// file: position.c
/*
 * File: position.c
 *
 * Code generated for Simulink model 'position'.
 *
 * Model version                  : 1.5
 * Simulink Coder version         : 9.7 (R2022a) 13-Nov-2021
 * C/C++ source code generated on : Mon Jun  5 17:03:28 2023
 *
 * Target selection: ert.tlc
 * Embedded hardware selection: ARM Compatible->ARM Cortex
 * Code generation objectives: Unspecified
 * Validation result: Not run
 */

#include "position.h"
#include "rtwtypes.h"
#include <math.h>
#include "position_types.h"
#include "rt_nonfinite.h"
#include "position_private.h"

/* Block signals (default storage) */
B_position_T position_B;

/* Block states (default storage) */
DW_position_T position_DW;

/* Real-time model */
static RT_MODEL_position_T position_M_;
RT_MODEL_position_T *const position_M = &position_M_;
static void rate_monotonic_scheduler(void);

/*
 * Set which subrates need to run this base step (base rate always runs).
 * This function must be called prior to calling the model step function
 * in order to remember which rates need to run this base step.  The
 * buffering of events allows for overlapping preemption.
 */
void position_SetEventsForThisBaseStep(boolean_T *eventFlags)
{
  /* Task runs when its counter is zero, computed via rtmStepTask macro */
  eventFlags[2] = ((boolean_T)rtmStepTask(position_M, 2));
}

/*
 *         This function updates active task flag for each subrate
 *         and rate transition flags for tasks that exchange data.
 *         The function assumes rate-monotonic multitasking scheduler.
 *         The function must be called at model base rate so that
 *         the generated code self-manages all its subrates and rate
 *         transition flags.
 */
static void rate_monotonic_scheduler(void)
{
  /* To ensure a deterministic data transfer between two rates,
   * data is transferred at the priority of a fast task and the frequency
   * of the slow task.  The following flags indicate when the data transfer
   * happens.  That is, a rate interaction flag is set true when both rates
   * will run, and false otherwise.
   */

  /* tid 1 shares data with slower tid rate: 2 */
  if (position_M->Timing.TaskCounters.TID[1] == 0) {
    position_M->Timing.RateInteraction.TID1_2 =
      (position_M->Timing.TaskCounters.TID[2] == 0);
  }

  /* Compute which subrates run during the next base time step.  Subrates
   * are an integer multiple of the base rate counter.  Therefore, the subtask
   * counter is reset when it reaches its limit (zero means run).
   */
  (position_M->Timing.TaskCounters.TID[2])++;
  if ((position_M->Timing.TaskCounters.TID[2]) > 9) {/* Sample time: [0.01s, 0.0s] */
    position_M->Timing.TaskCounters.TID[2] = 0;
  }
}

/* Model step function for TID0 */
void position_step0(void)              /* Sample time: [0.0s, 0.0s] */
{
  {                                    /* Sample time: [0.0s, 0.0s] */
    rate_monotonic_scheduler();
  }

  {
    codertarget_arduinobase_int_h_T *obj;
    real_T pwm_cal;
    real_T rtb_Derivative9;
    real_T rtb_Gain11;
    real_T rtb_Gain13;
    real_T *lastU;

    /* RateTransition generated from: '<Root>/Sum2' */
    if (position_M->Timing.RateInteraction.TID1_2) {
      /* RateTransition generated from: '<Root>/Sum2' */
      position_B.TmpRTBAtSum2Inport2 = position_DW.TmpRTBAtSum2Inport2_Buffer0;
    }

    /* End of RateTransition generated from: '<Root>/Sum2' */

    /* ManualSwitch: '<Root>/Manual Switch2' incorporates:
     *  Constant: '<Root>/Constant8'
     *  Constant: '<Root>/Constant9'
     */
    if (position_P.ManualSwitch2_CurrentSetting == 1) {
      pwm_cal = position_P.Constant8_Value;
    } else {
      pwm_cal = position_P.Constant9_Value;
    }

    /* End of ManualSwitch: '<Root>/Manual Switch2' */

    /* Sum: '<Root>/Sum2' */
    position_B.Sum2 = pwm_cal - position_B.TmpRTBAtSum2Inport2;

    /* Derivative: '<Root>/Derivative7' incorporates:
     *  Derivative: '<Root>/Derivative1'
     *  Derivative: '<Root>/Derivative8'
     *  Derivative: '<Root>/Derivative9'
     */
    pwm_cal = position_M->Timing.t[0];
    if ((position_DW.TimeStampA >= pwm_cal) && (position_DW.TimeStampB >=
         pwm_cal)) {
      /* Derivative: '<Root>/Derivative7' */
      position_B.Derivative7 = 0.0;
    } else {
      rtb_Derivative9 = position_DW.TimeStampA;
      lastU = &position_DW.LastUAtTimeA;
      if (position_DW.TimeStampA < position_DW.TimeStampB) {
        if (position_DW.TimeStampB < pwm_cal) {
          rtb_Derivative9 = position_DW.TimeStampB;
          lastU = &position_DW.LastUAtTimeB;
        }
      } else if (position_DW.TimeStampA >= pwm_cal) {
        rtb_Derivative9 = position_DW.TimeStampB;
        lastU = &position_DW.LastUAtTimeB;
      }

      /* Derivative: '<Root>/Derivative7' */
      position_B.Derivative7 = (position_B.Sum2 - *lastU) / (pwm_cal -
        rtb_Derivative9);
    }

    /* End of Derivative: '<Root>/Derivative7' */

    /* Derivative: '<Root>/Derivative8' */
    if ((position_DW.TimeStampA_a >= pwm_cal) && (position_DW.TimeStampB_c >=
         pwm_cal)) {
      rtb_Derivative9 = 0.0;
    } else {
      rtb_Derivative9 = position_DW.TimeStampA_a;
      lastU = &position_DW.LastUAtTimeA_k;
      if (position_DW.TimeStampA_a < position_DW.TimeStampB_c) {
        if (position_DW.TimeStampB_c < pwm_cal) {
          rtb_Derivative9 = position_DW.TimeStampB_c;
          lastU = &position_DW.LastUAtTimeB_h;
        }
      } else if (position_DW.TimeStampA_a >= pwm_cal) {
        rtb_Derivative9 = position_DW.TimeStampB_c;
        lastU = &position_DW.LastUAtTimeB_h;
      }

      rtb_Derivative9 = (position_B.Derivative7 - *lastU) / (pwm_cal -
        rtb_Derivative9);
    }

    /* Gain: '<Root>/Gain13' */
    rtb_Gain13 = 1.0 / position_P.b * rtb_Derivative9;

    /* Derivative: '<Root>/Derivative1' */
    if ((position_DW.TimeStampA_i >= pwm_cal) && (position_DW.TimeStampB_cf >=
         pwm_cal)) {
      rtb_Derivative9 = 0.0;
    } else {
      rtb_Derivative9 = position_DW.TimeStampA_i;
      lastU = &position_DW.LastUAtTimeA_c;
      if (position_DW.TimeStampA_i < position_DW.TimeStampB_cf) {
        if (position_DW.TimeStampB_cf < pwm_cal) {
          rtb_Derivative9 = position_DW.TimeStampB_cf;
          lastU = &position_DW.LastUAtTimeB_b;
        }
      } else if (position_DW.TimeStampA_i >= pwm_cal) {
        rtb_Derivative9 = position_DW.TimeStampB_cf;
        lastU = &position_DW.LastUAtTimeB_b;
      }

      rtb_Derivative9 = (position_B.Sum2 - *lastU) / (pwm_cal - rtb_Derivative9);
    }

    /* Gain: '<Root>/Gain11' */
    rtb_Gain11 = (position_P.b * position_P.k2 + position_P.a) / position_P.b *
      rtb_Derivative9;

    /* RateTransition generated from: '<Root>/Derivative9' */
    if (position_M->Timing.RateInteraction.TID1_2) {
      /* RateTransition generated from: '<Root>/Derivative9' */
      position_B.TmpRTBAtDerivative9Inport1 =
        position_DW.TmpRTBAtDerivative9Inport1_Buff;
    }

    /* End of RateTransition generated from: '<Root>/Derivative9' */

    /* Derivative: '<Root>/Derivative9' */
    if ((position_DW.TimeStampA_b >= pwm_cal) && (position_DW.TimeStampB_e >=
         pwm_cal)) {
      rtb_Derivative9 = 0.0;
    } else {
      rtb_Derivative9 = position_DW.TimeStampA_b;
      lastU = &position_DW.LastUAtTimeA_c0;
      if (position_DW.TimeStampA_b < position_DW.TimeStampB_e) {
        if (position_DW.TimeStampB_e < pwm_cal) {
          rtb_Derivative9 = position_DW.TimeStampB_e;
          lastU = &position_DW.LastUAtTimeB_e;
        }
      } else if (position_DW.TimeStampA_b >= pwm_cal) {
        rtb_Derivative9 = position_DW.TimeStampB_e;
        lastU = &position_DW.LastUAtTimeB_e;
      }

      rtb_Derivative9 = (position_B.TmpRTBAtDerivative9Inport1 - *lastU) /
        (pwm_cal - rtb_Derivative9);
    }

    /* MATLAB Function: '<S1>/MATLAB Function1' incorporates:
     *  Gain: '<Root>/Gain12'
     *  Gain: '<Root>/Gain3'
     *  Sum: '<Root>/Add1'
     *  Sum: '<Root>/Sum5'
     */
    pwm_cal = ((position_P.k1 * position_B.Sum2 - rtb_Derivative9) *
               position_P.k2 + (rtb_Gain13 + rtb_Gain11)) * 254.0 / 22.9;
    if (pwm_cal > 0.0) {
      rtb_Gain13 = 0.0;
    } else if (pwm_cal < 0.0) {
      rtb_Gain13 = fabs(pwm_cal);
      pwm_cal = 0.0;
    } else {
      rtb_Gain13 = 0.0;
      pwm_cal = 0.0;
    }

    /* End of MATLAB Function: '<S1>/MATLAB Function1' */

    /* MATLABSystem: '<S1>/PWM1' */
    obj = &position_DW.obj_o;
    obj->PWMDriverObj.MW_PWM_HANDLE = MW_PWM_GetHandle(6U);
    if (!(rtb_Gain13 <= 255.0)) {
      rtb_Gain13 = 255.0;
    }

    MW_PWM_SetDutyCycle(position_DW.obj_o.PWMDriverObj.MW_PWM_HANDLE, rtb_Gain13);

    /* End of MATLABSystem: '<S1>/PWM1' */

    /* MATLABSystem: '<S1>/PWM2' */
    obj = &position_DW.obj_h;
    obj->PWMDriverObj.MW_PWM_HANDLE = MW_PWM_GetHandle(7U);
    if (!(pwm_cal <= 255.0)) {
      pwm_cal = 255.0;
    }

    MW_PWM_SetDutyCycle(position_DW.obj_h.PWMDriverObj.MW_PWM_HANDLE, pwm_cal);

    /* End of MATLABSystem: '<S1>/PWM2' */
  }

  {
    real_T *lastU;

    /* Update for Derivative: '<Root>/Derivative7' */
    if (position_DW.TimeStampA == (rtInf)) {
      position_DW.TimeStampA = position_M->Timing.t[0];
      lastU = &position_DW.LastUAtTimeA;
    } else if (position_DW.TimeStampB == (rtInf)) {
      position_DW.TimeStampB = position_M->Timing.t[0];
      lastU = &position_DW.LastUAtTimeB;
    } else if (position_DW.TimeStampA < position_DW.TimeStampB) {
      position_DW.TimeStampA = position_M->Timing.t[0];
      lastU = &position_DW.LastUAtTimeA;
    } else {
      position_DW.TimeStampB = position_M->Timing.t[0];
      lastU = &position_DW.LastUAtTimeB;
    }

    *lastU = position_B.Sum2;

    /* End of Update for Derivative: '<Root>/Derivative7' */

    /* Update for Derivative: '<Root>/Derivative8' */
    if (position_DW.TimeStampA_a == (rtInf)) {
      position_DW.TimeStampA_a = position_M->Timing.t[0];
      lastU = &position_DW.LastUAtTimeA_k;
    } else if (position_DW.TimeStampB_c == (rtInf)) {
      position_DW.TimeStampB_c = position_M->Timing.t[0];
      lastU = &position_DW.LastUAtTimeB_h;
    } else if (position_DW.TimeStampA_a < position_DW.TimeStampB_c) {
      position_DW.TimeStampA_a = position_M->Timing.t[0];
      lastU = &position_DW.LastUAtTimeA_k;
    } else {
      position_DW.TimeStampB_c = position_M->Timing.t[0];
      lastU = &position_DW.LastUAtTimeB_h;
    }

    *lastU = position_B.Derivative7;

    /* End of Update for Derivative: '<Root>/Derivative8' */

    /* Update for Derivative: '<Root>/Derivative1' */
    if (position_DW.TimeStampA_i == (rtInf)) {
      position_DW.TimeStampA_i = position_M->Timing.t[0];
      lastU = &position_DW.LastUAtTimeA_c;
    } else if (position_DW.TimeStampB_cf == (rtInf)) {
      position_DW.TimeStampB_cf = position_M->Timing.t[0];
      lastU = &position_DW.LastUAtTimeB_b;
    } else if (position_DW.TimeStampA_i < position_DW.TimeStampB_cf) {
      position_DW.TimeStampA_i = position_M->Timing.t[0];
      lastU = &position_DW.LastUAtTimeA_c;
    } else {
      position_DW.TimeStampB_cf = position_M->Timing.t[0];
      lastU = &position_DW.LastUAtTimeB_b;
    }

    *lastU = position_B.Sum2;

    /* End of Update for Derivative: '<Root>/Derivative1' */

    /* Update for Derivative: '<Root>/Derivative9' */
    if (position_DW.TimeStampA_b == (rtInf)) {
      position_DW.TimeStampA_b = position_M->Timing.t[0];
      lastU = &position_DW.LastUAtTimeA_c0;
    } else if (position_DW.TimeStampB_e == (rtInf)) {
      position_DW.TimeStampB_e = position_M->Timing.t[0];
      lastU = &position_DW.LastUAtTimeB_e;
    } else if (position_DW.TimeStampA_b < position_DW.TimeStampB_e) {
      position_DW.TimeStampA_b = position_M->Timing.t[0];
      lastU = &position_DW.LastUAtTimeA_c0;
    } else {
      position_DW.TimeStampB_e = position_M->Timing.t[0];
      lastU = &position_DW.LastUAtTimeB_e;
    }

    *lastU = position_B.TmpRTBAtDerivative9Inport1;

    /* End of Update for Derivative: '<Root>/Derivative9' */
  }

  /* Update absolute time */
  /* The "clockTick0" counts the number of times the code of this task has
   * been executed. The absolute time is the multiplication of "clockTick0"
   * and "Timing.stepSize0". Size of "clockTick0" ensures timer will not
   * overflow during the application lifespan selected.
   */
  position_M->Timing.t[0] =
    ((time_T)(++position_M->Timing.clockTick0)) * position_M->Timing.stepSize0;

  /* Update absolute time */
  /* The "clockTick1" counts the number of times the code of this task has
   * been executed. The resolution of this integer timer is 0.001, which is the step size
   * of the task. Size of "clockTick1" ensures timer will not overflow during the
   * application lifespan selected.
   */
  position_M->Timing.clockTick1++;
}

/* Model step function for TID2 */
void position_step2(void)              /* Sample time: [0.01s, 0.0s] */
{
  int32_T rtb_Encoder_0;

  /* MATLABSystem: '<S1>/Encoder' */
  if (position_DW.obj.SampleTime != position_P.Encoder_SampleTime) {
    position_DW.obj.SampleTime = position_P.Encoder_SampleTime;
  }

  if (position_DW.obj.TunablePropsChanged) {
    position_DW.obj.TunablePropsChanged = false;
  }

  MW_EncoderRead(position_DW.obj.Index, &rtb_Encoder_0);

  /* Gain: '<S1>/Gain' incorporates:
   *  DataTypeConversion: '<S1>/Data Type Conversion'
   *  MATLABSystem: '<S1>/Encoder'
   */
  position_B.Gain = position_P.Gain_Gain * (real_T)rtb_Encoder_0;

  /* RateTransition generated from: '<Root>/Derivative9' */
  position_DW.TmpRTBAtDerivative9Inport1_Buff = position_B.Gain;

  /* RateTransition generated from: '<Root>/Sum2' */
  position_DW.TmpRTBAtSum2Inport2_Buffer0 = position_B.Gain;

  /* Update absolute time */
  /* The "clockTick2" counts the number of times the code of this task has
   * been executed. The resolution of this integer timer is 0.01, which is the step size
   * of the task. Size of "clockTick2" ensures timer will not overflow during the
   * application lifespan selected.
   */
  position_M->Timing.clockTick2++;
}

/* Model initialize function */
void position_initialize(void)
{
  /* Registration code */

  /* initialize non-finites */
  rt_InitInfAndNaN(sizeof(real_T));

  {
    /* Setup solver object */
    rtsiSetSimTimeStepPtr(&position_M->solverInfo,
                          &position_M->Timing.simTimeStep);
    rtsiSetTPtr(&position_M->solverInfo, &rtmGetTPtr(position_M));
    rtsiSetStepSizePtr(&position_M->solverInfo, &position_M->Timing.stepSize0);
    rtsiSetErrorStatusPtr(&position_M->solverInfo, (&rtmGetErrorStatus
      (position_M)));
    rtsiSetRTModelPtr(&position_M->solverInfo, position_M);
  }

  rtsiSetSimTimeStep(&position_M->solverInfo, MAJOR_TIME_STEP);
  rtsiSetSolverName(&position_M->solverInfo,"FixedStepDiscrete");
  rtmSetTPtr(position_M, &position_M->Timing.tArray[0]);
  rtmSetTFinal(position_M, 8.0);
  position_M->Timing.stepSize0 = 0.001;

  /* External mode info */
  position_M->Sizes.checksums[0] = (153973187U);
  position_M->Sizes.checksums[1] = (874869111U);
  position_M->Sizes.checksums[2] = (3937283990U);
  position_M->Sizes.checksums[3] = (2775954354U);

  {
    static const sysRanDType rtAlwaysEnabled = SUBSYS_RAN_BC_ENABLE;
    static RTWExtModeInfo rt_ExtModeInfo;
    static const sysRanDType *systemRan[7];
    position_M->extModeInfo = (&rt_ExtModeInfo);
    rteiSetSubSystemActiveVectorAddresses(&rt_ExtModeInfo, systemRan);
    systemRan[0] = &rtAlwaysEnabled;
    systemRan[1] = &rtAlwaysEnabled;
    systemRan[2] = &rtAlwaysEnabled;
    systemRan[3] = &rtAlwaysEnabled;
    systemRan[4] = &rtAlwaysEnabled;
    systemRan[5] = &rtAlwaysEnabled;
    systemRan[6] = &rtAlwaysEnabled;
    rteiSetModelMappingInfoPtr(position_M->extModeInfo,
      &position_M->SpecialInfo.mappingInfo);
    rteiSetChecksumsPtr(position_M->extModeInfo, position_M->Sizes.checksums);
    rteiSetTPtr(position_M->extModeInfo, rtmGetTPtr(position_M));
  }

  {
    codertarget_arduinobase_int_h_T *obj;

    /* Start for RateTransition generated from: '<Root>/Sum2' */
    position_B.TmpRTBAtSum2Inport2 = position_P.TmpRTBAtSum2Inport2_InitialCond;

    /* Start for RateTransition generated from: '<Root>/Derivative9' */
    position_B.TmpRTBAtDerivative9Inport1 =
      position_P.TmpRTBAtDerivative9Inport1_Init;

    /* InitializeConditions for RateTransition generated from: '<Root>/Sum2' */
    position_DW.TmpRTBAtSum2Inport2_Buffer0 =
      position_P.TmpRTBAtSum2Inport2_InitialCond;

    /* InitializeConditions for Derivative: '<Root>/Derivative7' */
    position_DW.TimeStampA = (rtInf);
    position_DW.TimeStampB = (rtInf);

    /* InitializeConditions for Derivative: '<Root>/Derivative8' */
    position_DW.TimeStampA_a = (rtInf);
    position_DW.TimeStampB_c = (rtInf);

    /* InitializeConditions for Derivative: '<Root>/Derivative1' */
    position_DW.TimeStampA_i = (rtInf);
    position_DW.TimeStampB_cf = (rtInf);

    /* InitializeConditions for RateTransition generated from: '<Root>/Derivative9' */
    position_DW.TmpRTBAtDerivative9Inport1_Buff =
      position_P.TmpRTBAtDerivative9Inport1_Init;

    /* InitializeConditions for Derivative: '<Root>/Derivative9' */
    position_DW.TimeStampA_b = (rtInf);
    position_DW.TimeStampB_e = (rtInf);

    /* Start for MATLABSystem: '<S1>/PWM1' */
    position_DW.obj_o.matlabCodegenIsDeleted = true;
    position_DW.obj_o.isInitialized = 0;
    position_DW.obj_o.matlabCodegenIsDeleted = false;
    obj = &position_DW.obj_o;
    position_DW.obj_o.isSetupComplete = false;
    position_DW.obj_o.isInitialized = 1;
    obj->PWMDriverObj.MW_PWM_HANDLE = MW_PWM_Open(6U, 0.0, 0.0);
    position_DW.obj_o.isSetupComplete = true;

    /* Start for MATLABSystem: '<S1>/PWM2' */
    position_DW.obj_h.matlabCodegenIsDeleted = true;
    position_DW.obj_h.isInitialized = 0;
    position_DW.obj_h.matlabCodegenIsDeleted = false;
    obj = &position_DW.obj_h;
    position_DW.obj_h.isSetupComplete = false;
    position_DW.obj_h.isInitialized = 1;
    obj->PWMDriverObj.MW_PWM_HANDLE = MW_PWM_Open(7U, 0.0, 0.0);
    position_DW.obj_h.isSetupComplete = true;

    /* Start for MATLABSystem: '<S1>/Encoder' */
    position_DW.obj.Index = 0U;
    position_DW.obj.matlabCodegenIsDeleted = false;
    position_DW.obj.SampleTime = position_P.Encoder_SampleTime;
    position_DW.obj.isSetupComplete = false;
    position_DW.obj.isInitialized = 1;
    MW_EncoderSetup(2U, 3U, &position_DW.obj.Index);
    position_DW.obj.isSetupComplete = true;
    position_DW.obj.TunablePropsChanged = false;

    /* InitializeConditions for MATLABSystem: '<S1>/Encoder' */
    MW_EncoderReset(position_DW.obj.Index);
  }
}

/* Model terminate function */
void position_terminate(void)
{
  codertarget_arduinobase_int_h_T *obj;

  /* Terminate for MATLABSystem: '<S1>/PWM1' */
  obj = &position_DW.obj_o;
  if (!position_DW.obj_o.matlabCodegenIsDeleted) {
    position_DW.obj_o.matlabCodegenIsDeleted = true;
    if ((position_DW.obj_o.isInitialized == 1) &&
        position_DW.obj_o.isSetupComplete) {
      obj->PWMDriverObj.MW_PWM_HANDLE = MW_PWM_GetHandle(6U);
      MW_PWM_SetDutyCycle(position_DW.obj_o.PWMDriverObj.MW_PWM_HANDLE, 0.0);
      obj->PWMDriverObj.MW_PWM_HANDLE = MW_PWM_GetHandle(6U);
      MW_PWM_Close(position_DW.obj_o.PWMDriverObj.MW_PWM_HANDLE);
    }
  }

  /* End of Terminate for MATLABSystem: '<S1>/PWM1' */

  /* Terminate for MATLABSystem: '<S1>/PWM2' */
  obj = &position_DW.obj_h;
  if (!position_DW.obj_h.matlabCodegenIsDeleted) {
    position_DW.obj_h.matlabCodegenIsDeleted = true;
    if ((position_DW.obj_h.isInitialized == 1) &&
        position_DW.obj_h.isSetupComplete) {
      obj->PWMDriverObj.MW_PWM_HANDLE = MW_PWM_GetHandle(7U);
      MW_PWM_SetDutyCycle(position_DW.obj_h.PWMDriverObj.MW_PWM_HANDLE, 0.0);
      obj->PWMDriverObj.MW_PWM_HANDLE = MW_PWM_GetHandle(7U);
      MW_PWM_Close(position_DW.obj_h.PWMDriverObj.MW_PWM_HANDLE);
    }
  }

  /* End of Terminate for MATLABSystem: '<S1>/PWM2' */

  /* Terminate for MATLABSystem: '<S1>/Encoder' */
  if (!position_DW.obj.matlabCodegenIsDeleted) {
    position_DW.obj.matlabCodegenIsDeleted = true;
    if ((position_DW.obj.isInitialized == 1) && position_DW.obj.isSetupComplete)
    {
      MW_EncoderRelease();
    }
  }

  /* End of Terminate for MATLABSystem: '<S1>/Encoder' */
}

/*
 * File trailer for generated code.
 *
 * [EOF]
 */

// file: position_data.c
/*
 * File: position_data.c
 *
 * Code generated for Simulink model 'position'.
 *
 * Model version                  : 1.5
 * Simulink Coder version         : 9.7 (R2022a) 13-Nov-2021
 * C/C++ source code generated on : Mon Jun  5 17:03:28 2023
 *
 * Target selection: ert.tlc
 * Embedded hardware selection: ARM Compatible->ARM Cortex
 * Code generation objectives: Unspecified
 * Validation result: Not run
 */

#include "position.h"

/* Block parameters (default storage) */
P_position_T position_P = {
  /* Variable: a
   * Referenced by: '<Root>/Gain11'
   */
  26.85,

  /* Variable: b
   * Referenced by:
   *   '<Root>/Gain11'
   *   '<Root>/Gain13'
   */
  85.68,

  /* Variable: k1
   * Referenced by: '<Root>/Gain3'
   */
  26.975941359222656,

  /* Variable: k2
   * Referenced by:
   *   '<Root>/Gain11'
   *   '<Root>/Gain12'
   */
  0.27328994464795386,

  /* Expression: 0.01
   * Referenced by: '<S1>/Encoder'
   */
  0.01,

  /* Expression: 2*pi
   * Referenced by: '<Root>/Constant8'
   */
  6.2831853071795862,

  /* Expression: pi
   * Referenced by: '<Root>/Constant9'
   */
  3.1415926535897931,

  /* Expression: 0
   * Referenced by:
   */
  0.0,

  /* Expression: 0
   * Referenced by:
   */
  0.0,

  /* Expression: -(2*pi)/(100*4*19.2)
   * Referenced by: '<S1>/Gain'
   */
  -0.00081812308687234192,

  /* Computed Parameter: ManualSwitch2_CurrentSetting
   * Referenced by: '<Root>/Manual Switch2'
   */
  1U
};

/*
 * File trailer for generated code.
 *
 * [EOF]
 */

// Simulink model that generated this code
simulink model "position"  (R2022a)
settings: Solver=ode1  StartTime=0.0  StopTime=8  FixedStep=0.001  RelTol=1e-3  EnableMultiTasking=on
undefined symbols (not defined in the file): a, b, k1, k2
libraries: arduinolib x4, arduinosensorlib x1

== system position ==
  note: $\theta$
  Add1 : Sum  Inputs=+++
  Constant8 : Constant  Value=2*pi
  Constant9 : Constant  Value=pi
  Derivative{1,7..9} (4 alike) : Derivative
  Gain11 : Gain  Gain=(a+b*k2)/b
  Gain12 : Gain  Gain=k2
  Gain13 : Gain  Gain=1/b
  Gain3 : Gain  Gain=k1
  Manual Switch2 : ManualSwitch
  Right motor1 : Subsystem
  Scope1 : Scope
  Scope7 : Scope
  Sum2 : Sum  Inputs=|+-
  Sum5 : Sum  Inputs=|+-
  wires:
  Right motor1/1(outGearBox) -> Sum2/2, Derivative9/1, Scope7/1
  Derivative8/1 -> Gain13/1
  Add1/1 -> Right motor1/1(v_a)
  Constant9/1 -> Manual Switch2/2
  Sum2/1 -> Scope1/1, Derivative7/1, Derivative1/1, Gain3/1
  Gain11/1 -> Add1/2
  Derivative9/1 -> Sum5/2
  Manual Switch2/1 -> Sum2/1
  Derivative1/1 -> Gain11/1
  Gain3/1 -> Sum5/1
  Constant8/1 -> Manual Switch2/1
  Gain13/1 -> Add1/1
  Derivative7/1 -> Derivative8/1
  Gain12/1 -> Add1/3
  Sum5/1 -> Gain12/1

== system position/Right motor1 ==
  v_a : Inport
  Convert pulse to rad1 : MATLAB Function  Commented=on  TreatAsAtomicUnit=on
  Data Type Conversion : DataTypeConversion  OutDataTypeStr=double  SaturateOnIntegerOverflow=off  RndMeth=Floor
  Digital Output : arduinolib/Digital Output  Commented=on  pinNumber=7  Direction=output  blockPlatform=arduino
  Encoder : arduinosensorlib/Encoder  InputA=2  InputB=3  Mode=No reset  SampleTime=0.01
  Encoder1 : S-Function  Commented=on  InitFcn=try, set_param(gcb,'FunctionName','readEncDUEpin8_9'), end  FunctionName=readEncDUEpin8_9  SFunctionModules=readEncDUEpin8_9_wrapper  SFunctionDeploymentMode=off  EnableBusSupport=off  mask(S-Function Builder){}
      mask help: Simulink:masks:SFunctionBuilder_MD
      mask init:
      | val = [[.9  0.75 0.75 1 1 .9 .9 1]',[1 1 0.75 0.75 .9 .9 1 .9]'];try , sys = get_param(gcb,'SfunBuilderFcnName');if isempty(sys), sys = get_param(gcb,'FunctionName'); end,catch, sys = get_param(gcb,'FunctionName'); end
  Gain : Gain  Gain=-(2*pi)/(100*4*19.2)
  MATLAB Function1 : MATLAB Function  TreatAsAtomicUnit=on
  MATLAB Function2 : MATLAB Function  Commented=on  TreatAsAtomicUnit=on
  PWM : arduinolib/PWM  Commented=on  pinNumber=5  frequencyType=Default  desiredFrequency=490.2  achievableFrequency=490.2
  PWM1 : arduinolib/PWM  pinNumber=6  frequencyType=Default  desiredFrequency=490.2  achievableFrequency=490.2
  PWM2 : arduinolib/PWM  pinNumber=7  frequencyType=Default  desiredFrequency=490.2  achievableFrequency=490.2
  Scope : Scope  Commented=on
  Scope1 : Scope
  gearRatio : Constant  Commented=on  Value=336
  totalPPR : Constant  Commented=on  Value=16*2
  outGearBox : Outport
  wires:
  Gain/1 -> Scope1/1, outGearBox/1
  Encoder/1 -> Data Type Conversion/1
  v_a/1 -> MATLAB Function1/1(v_a)
  MATLAB Function1/2(Rpwm) -> PWM2/1
  MATLAB Function1/1(Lpwm) -> PWM1/1
  Encoder1/1 -> Convert pulse to rad1/1(u)
  Convert pulse to rad1/1(outGearBox) -> Scope/1
  gearRatio/1 -> Convert pulse to rad1/3(gearRatio)
  MATLAB Function2/1(pwm) -> PWM/1
  MATLAB Function2/2(dir) -> Digital Output/1
  totalPPR/1 -> Convert pulse to rad1/2(ppr)
  Data Type Conversion/1 -> Gain/1

== matlab function position/Right motor1/Convert pulse to rad1 ==
  settings: updateMethod=DISCRETE
function outGearBox = fcn(u,ppr,gearRatio)

persistent counter_num over_flag
if(isempty(counter_num)), counter_num = 0;end
if(isempty(over_flag)), over_flag = 0;end
pulse2radian = 2*pi/ppr; % 1 pulse = ?? radian

if(double(u) - counter_num > 40000), over_flag = over_flag-1;
elseif(double(u) - counter_num < -40000), over_flag = over_flag+1;
end

inGearBox = (double(u)+over_flag*(2^32 -1))*pulse2radian; 
outGearBox = inGearBox/gearRatio;
counter_num = double(u) ;

== matlab function position/Right motor1/MATLAB Function1 ==
function [Lpwm,Rpwm] = fcn(v_a)

vmax = 22.9;
pwm_cal = v_a*254/vmax;

if pwm_cal > 0
    Lpwm = 0;
    Rpwm = pwm_cal;
elseif pwm_cal < 0
    Lpwm = abs(pwm_cal);
    Rpwm = 0;
else
    Lpwm = 0;
    Rpwm = 0;
end

== matlab function position/Right motor1/MATLAB Function2 ==
function [pwm,dir] = fcn(v_a)

vmax = 22.9;
%vmax = 10;
pwm_cal = v_a*254/vmax;
if pwm_cal > 0
    pwm = pwm_cal;
    dir = 0;
elseif pwm_cal < 0
    pwm = abs(pwm_cal);
    dir = 1;
else
    pwm = 0;
    dir = 0;
end
